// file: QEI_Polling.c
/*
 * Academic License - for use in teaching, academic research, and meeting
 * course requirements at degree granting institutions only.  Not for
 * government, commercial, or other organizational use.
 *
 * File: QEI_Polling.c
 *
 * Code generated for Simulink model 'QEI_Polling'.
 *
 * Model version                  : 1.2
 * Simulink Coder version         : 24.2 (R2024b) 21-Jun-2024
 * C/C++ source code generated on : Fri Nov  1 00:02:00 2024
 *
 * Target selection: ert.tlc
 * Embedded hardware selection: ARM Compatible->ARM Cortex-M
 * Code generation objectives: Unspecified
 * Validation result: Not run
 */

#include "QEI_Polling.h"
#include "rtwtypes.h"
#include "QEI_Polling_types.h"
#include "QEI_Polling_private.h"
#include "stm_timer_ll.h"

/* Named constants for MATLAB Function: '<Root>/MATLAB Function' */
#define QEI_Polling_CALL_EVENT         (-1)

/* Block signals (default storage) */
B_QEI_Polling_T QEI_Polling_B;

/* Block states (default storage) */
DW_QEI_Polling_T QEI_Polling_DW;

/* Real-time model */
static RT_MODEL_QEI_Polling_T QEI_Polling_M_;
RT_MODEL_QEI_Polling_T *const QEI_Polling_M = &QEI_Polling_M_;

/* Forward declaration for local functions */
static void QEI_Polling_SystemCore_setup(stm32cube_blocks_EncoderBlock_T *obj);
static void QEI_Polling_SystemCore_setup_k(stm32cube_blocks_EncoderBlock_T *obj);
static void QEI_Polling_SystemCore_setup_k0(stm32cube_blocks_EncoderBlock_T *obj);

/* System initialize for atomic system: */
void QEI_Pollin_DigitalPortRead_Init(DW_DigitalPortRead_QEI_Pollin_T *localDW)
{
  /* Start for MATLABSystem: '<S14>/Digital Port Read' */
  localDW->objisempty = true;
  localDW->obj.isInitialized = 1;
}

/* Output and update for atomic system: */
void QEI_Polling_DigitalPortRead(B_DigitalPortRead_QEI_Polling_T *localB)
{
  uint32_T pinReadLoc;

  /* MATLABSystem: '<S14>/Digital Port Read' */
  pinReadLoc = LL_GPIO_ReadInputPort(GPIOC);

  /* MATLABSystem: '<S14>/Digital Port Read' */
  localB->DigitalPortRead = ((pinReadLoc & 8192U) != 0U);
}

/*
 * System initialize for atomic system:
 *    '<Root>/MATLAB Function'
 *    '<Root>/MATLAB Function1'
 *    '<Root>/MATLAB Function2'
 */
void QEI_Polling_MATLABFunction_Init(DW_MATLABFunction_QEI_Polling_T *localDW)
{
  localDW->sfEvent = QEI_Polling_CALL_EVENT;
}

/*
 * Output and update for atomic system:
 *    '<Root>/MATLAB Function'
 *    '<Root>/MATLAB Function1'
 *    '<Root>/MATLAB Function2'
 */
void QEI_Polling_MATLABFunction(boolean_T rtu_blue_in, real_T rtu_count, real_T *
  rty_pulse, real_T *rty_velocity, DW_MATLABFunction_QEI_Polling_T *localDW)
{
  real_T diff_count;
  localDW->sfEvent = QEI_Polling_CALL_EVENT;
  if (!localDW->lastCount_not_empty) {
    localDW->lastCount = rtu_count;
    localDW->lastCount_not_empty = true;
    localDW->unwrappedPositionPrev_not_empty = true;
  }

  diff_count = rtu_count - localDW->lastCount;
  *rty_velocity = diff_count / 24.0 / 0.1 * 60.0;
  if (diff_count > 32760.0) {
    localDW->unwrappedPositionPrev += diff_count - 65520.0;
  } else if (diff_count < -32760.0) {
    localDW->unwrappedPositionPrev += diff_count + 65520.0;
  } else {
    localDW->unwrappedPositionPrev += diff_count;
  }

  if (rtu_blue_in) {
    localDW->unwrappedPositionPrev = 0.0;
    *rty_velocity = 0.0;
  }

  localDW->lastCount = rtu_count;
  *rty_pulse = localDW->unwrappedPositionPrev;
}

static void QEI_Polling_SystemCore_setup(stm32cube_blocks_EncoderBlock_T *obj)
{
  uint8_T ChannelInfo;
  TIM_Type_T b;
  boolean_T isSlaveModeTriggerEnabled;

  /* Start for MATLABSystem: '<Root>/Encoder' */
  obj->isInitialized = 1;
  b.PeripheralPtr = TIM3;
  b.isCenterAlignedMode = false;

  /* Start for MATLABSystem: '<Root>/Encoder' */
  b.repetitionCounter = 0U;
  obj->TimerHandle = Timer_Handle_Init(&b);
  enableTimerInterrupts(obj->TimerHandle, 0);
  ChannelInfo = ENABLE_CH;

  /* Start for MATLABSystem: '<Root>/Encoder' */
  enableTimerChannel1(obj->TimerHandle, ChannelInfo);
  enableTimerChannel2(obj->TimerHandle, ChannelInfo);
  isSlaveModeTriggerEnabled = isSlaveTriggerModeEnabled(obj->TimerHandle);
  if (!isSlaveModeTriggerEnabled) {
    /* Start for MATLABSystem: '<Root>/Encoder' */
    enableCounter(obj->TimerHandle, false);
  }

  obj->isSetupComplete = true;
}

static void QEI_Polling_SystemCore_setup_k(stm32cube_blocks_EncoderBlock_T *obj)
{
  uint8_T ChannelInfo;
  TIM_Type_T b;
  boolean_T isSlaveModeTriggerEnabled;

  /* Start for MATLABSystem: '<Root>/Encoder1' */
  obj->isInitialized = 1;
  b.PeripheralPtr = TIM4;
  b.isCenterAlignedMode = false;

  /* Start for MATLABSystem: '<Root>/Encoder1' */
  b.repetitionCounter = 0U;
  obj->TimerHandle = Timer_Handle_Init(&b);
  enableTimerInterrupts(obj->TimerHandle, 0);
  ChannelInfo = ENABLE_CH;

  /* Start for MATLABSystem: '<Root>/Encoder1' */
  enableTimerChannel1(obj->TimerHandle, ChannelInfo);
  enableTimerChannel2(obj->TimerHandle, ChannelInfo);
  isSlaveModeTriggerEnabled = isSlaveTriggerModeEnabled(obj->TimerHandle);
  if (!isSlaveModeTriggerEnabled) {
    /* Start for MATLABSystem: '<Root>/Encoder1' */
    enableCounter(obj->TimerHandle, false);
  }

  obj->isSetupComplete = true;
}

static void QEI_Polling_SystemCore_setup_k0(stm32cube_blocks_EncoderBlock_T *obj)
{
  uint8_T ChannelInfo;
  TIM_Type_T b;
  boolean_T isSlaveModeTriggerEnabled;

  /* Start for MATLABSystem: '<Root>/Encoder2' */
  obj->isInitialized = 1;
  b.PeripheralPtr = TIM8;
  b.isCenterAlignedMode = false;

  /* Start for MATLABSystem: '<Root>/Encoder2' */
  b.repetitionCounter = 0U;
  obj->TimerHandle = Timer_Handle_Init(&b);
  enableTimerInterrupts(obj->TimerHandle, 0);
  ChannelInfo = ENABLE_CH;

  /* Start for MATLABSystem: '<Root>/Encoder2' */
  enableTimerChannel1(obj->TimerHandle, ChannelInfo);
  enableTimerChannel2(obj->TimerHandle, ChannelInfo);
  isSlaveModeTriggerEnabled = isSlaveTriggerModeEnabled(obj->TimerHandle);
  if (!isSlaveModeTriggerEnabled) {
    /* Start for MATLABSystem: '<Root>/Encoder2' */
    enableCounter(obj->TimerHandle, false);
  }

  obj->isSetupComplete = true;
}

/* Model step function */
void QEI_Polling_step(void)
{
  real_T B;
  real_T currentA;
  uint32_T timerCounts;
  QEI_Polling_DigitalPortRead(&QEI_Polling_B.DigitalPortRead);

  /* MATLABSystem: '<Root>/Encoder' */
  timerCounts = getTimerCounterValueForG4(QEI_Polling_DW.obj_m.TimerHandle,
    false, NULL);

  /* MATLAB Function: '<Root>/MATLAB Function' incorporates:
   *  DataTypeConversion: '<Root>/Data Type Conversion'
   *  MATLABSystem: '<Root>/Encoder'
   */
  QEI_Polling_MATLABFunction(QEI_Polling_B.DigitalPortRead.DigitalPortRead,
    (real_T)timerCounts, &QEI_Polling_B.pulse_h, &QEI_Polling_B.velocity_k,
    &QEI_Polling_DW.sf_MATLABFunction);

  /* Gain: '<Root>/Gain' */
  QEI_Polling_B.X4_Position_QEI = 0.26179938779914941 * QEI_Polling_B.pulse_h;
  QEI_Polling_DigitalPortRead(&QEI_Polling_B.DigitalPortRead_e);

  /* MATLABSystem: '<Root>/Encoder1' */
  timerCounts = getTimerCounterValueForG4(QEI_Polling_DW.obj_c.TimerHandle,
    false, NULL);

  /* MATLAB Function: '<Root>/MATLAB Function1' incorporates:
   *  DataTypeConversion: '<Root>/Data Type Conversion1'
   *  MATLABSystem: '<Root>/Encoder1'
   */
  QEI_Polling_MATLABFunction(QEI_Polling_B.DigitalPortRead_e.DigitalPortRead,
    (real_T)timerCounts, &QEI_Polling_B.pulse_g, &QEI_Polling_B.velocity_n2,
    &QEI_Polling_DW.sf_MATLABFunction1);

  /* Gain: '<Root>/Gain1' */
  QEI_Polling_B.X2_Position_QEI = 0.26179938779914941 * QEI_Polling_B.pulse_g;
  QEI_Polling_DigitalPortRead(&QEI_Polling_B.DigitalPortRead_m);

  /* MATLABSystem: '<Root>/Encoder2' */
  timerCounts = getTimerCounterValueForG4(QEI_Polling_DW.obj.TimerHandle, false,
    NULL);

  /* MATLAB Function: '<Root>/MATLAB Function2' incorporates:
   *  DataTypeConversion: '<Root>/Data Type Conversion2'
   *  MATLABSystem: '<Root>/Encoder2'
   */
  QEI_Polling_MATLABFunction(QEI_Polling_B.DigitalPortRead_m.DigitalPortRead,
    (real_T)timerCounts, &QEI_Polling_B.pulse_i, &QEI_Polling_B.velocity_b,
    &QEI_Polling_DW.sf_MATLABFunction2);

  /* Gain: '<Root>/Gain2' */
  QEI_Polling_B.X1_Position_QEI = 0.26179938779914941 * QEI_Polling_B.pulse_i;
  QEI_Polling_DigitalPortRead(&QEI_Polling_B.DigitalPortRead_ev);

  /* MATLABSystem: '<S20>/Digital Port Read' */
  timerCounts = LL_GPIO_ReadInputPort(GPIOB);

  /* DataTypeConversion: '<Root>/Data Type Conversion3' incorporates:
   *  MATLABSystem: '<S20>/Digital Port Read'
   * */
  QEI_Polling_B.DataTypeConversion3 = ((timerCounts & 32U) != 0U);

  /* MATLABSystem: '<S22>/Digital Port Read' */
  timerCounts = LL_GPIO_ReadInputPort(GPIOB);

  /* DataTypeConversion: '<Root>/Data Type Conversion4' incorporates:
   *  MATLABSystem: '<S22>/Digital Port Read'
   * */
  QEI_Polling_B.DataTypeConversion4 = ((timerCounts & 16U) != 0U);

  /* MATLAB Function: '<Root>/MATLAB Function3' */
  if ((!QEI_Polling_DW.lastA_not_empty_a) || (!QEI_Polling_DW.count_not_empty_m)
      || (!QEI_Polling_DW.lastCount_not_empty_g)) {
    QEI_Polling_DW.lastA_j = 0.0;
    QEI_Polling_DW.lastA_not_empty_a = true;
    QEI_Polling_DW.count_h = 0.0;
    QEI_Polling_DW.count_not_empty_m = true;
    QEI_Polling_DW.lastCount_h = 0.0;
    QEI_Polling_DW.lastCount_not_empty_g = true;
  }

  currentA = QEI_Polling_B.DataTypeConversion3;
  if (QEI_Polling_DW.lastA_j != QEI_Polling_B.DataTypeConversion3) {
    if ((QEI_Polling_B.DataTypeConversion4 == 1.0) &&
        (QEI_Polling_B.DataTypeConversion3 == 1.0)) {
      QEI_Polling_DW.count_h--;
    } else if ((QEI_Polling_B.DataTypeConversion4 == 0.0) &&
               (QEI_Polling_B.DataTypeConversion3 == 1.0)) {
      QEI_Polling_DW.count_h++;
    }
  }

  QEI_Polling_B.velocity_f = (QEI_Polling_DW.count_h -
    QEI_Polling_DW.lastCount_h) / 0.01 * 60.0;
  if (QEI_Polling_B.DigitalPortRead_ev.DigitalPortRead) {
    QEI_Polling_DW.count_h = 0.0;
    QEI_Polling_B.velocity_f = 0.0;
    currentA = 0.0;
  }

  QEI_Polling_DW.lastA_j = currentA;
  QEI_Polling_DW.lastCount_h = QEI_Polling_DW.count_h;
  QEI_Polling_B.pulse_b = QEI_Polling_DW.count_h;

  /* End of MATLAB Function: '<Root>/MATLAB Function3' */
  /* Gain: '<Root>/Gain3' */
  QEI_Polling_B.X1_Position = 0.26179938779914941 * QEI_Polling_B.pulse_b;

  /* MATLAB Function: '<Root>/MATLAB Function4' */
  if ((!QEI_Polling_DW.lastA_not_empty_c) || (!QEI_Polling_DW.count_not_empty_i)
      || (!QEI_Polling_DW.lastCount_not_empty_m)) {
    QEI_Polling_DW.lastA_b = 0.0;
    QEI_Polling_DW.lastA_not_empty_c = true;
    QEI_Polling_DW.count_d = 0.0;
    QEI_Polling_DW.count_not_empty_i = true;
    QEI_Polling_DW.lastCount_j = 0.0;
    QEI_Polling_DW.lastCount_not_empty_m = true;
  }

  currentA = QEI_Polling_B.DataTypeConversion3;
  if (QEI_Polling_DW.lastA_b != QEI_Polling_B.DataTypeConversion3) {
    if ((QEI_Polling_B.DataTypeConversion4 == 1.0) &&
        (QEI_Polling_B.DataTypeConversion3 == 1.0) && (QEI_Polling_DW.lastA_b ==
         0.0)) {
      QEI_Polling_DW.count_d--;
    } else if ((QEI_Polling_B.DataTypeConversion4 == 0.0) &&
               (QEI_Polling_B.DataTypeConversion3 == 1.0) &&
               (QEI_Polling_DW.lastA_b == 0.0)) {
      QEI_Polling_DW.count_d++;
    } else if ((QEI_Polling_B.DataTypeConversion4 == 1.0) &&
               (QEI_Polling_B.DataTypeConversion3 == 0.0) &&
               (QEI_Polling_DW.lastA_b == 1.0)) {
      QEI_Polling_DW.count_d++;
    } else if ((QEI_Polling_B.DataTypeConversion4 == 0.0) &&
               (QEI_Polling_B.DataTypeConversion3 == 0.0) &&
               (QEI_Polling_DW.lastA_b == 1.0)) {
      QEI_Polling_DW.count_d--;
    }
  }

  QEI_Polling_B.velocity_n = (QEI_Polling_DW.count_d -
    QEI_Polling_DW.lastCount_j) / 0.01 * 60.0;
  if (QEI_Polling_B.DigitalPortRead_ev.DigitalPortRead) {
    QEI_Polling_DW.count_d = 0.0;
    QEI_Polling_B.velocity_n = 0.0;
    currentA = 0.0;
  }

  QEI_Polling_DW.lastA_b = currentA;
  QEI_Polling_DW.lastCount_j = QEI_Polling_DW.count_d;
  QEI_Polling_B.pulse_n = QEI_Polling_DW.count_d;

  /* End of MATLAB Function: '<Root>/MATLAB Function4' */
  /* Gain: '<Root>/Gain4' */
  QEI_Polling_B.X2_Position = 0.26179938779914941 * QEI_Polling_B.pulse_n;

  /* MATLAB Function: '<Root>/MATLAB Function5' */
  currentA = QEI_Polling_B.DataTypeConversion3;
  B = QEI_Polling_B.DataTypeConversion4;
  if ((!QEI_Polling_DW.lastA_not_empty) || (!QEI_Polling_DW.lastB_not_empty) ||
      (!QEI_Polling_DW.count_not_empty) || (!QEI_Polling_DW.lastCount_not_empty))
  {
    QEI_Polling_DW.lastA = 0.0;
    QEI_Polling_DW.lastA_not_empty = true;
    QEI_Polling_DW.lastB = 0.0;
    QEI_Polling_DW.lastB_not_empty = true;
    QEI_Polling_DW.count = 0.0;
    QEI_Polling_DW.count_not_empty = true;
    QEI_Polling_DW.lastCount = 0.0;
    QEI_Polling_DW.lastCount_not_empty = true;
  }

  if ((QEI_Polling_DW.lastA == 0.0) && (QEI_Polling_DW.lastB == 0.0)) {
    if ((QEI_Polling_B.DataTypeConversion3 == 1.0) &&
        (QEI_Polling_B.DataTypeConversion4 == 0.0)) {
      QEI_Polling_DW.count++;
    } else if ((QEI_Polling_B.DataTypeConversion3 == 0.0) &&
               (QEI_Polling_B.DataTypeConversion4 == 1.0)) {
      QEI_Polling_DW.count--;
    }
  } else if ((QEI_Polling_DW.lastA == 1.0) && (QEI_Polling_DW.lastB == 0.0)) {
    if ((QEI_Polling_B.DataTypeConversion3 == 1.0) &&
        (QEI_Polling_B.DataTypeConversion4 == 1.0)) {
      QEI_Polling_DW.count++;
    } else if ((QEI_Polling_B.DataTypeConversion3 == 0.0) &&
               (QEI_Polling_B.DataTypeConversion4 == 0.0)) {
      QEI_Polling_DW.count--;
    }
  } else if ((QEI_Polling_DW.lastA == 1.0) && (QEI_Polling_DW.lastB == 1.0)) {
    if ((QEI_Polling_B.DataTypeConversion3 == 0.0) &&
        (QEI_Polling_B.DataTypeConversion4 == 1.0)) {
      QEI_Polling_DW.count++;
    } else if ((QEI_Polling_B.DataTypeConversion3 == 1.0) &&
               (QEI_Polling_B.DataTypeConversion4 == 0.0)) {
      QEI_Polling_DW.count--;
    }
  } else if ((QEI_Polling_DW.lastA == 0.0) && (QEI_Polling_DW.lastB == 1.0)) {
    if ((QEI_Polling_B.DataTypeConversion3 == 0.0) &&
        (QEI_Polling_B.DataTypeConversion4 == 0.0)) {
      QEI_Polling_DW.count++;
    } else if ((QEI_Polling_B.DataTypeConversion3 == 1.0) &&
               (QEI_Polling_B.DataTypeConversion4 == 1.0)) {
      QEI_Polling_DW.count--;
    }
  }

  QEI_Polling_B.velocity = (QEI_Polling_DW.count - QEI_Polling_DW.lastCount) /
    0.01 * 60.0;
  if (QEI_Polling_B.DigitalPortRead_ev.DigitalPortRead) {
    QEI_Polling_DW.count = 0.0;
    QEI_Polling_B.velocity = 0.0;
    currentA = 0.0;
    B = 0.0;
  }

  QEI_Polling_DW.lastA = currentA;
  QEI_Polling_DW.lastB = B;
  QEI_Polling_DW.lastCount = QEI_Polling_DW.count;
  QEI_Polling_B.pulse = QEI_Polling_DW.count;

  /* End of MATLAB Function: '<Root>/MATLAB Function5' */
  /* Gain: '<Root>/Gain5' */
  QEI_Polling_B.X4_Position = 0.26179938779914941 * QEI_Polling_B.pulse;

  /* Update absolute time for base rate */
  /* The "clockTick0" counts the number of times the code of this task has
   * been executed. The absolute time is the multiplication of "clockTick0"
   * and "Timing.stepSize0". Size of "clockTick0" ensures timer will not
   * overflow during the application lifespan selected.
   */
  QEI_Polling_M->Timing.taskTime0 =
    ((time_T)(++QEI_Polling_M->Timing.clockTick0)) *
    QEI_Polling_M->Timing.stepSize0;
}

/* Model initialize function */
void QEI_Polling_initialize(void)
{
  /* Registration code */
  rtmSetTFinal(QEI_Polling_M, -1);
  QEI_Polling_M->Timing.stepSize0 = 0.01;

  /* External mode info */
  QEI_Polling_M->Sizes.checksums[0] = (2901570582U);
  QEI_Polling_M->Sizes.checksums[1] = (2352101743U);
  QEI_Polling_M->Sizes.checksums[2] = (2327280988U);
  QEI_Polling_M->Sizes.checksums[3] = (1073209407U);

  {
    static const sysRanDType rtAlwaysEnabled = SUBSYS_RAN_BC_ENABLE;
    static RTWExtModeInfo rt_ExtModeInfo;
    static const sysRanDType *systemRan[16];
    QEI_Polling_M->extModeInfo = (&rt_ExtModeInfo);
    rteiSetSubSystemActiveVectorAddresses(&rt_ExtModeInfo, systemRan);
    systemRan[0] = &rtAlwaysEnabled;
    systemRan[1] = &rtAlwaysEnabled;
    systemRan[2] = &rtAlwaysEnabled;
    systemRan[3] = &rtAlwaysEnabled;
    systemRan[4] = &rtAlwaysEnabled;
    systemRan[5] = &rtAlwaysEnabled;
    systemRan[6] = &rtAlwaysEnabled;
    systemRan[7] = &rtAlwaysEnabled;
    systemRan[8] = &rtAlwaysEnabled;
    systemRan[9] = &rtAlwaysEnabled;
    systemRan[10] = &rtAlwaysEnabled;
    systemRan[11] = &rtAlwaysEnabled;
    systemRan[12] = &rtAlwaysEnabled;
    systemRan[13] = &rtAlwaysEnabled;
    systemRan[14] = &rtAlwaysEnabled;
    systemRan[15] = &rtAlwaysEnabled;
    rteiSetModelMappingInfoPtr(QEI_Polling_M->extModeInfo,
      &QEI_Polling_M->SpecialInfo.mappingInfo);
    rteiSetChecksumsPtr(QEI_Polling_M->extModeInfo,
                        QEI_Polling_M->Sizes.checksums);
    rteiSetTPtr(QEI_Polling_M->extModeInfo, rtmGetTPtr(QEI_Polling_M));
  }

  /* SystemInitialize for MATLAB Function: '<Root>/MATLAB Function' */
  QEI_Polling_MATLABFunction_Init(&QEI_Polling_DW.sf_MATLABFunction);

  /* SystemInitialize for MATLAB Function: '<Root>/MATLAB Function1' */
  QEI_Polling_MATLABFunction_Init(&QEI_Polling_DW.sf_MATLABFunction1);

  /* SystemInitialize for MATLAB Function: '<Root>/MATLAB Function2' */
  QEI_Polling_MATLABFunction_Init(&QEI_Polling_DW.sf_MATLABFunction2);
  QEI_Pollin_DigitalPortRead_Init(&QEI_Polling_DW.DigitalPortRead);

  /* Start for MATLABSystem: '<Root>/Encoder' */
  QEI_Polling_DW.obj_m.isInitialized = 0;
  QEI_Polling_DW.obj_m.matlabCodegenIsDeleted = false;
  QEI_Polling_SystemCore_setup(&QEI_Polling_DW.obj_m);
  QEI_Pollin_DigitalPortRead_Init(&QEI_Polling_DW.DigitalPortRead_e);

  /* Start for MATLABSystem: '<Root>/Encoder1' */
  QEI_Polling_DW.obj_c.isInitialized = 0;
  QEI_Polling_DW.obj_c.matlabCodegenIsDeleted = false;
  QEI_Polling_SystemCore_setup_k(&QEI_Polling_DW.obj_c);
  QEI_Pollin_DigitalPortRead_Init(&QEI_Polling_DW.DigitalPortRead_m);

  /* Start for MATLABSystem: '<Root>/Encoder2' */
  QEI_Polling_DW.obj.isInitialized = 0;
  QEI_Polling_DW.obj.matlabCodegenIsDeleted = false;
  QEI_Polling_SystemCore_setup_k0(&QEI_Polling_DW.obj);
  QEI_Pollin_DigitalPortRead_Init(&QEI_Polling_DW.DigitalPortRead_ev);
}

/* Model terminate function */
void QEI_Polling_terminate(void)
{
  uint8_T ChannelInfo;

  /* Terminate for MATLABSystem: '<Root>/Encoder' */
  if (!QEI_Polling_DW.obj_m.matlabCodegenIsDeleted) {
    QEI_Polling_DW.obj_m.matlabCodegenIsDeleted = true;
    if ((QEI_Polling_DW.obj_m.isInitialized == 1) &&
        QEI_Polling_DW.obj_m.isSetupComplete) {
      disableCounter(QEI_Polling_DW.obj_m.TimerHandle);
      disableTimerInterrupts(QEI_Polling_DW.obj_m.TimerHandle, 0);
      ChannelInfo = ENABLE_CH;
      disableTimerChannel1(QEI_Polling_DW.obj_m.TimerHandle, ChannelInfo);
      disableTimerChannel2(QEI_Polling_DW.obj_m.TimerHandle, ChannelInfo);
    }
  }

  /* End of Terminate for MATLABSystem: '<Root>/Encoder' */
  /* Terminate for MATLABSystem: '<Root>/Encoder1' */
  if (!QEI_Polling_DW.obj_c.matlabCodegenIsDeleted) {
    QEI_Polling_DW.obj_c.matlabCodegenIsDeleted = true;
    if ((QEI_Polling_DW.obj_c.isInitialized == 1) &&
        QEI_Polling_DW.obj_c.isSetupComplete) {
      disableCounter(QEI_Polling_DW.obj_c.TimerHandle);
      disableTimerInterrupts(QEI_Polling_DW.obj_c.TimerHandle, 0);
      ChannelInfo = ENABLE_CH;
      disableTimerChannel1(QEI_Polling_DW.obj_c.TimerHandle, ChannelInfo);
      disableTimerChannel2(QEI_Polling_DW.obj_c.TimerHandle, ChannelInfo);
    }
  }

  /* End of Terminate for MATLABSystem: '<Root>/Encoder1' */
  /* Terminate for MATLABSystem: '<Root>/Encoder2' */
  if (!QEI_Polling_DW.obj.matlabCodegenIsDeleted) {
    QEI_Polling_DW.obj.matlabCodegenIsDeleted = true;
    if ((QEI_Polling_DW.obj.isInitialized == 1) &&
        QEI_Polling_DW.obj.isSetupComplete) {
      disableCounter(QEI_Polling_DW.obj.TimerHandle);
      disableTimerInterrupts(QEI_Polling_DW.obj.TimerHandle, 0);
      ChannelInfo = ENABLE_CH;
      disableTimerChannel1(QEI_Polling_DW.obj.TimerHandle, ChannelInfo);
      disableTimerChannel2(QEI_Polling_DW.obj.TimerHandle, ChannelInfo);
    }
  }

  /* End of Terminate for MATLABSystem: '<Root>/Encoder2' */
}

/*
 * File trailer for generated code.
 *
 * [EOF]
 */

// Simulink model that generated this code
simulink model "QEI_Polling"  (R2024b)
settings: Solver=FixedStepAuto  StartTime=0.0  StopTime=inf  FixedStep=0.001  RelTol=1e-3  EnableMultiTasking=on
libraries: stm32f4xxblockslib x5, stm32g4xxblockslib x3

== system QEI_Polling ==
  note: QEI
  Data Type Conversion{,1..4} (5 alike) : DataTypeConversion  OutDataTypeStr=double  SaturateOnIntegerOverflow=off  RndMeth=Floor
  Digital Port Read : stm32f4xxblockslib/Digital Port Read  PortName=GPIOC  PinNumber=[13]  ReadOperation=on  IOAsArray=on  SampleTime=-1  EnableSimPort=off  hoistedMaskSrc=ECSoC/ECSimCodegen/Digital Port Read
  Digital Port Read1 : stm32f4xxblockslib/Digital Port Read  PortName=GPIOC  PinNumber=[13]  ReadOperation=on  IOAsArray=on  SampleTime=-1  EnableSimPort=off  hoistedMaskSrc=ECSoC/ECSimCodegen/Digital Port Read
  Digital Port Read2 : stm32f4xxblockslib/Digital Port Read  PortName=GPIOC  PinNumber=[13]  ReadOperation=on  IOAsArray=on  SampleTime=-1  EnableSimPort=off  hoistedMaskSrc=ECSoC/ECSimCodegen/Digital Port Read
  Digital Port Read3 : stm32f4xxblockslib/Digital Port Read  PortName=GPIOB  PinNumber=[5]  ReadOperation=on  IOAsArray=on  SampleTime=-1  EnableSimPort=off  hoistedMaskSrc=ECSoC/ECSimCodegen/Digital Port Read
  Digital Port Read4 : stm32f4xxblockslib/Digital Port Read  PortName=GPIOB  PinNumber=[4]  ReadOperation=on  IOAsArray=on  SampleTime=-1  EnableSimPort=off  hoistedMaskSrc=ECSoC/ECSimCodegen/Digital Port Read
  Display{,1..17} (18 alike) : Display
  Encoder : stm32g4xxblockslib/Encoder  TimerModule=TIM3  EnableResetInput=off  OutputCountAfterFirstIndex=off  OutputValidIndex=off  OutputDirection=off  OutputStatus=off  SampleTime=-1
  Encoder1 : stm32g4xxblockslib/Encoder  TimerModule=TIM4  EnableResetInput=off  OutputCountAfterFirstIndex=off  OutputValidIndex=off  OutputDirection=off  OutputStatus=off  SampleTime=-1
  Encoder2 : stm32g4xxblockslib/Encoder  TimerModule=TIM8  EnableResetInput=off  OutputCountAfterFirstIndex=off  OutputValidIndex=off  OutputDirection=off  OutputStatus=off  SampleTime=-1
  Gain{,1..5} (6 alike) : Gain  Gain=(2 * pi)/24
  MATLAB Function : MATLAB Function  TreatAsAtomicUnit=on
  MATLAB Function1 : MATLAB Function  TreatAsAtomicUnit=on
  MATLAB Function2 : MATLAB Function  TreatAsAtomicUnit=on
  MATLAB Function3 : MATLAB Function  TreatAsAtomicUnit=on
  MATLAB Function4 : MATLAB Function  TreatAsAtomicUnit=on
  MATLAB Function5 : MATLAB Function  TreatAsAtomicUnit=on
  wires:
  Data Type Conversion/1 -> MATLAB Function/2(count)
  Encoder1/1 -> Data Type Conversion1/1
  Gain3/1 -> Display10/1  "X1_Position"
  MATLAB Function2/2(velocity) -> Display7/1  "X1_Velocity_QEI"
  MATLAB Function3/2(velocity) -> Display9/1  "X1_Velocity"
  Data Type Conversion3/1 -> MATLAB Function4/1(A), MATLAB Function5/1(A), MATLAB Function3/1(A)
  Data Type Conversion2/1 -> MATLAB Function2/2(count)
  MATLAB Function3/1(pulse) -> Display11/1, Gain3/1  "X1_Pulse"
  Digital Port Read1/1 -> MATLAB Function1/1(blue_in)
  Encoder2/1 -> Data Type Conversion2/1
  Digital Port Read/1 -> MATLAB Function/1(blue_in)
  Digital Port Read4/1 -> Data Type Conversion4/1
  MATLAB Function5/1(pulse) -> Display16/1, Gain5/1  "X4_Pulse"
  MATLAB Function/1(pulse) -> Display2/1, Gain/1  "X4_Pulse_QEI"
  Gain5/1 -> Display15/1  "X4_Position"
  Data Type Conversion1/1 -> MATLAB Function1/2(count)
  MATLAB Function1/2(velocity) -> Display4/1  "X2_Velocity_QEI"
  Data Type Conversion4/1 -> MATLAB Function4/2(B), MATLAB Function5/2(B), MATLAB Function3/2(B)
  Gain1/1 -> Display3/1  "X2_Position_QEI"
  Digital Port Read3/1 -> Data Type Conversion3/1
  MATLAB Function4/1(pulse) -> Display13/1, Gain4/1  "X2_Pulse"
  Encoder/1 -> Data Type Conversion/1
  Digital Port Read2/1 -> MATLAB Function2/1(blue_in)
  MATLAB Function5/2(velocity) -> Display17/1  "X4_Velocity"
  MATLAB Function1/1(pulse) -> Display5/1, Gain1/1  "X2_Pulse_QEI"
  Gain/1 -> Display/1  "X4_Position_QEI"
  MATLAB Function/2(velocity) -> Display1/1  "X4_Velocity_QEI"
  Gain4/1 -> Display12/1  "X2_Position"
  Gain2/1 -> Display6/1  "X1_Position_QEI"
  MATLAB Function4/2(velocity) -> Display14/1  "X2_Velocity"
  MATLAB Function2/1(pulse) -> Display8/1, Gain2/1  "X1_Pulse_QEI"

== matlab function QEI_Polling/MATLAB Function1 ==
function [pulse, velocity] = X4(blue_in, count)
    %#codegen
    
    % ประกาศตัวแปร persistent เพื่อเก็บค่าตัวนับก่อนหน้าและตำแหน่งที่คลายห่อก่อนหน้า
    persistent previousCount unwrappedPositionPrev;
    
    % กำหนดค่าเริ่มต้นให้ตัวแปร persistent เมื่อเรียกใช้งานครั้งแรก
    if isempty(previousCount)
        previousCount = count;
        unwrappedPositionPrev = 0;  % กำหนดตำแหน่งคลายห่อเริ่มต้นเป็นศูนย์
    end

    % กำหนดขอบเขตของ encoder
    encoderMax = 65520;   % ค่าสูงสุดสำหรับ encoder แบบ 16-bit (0-65535)
    threshold = encoderMax / 2;  % ค่า threshold สำหรับตรวจจับ overflow หรือ underflow

    % คำนวณค่าความแตกต่างระหว่างค่าปัจจุบันกับค่าก่อนหน้า
    diff_count = count - previousCount;

    % คำนวณความเร็วเชิงมุม (Angular Velocity)
    Ts = 0.01; % กำหนด Sampling Time (เช่น 10ms)
    PPR = 24; % จำนวนพัลส์ต่อรอบ
    velocity = ((diff_count / PPR) / Ts) * 60; % Velocity เป็น RPM

    % ตรวจจับการ overflow และ underflow
    if diff_count > threshold
        % พบการ overflow (เช่น count เปลี่ยนจาก 65535 กลับไปที่ 0)
        pulse = unwrappedPositionPrev + (diff_count - encoderMax);
    elseif diff_count < -threshold
        % พบการ underflow (เช่น count เปลี่ยนจาก 0 เป็น 65535)
        pulse = unwrappedPositionPrev + (diff_count + encoderMax);
    else
        % กรณีปกติที่ไม่มี overflow/underflow
        pulse = unwrappedPositionPrev + diff_count;
    end

    if blue_in == 1
        pulse = 0;
        velocity = 0;
    end
    % อัปเดตตัวแปร persistent เพื่อใช้ในรอบถัดไป
    previousCount = count;
    unwrappedPositionPrev = pulse; 
end

== matlab function QEI_Polling/MATLAB Function ==
function [pulse, velocity] = X4(blue_in, count)
    %#codegen
    
    % ประกาศตัวแปร persistent เพื่อเก็บค่าตัวนับก่อนหน้าและตำแหน่งที่คลายห่อก่อนหน้า
    persistent previousCount unwrappedPositionPrev;
    
    % กำหนดค่าเริ่มต้นให้ตัวแปร persistent เมื่อเรียกใช้งานครั้งแรก
    if isempty(previousCount)
        previousCount = count;
        unwrappedPositionPrev = 0;  % กำหนดตำแหน่งคลายห่อเริ่มต้นเป็นศูนย์
    end

    % กำหนดขอบเขตของ encoder
    encoderMax = 65520;   % ค่าสูงสุดสำหรับ encoder แบบ 16-bit (0-65535)
    threshold = encoderMax / 2;  % ค่า threshold สำหรับตรวจจับ overflow หรือ underflow

    % คำนวณค่าความแตกต่างระหว่างค่าปัจจุบันกับค่าก่อนหน้า
    diff_count = count - previousCount;

    % คำนวณความเร็วเชิงมุม (Angular Velocity)
    Ts = 0.01; % กำหนด Sampling Time (เช่น 10ms)
    PPR = 24; % จำนวนพัลส์ต่อรอบ
    velocity = ((diff_count / PPR) / Ts) * 60; % Velocity เป็น RPM

    % ตรวจจับการ overflow และ underflow
    if diff_count > threshold
        % พบการ overflow (เช่น count เปลี่ยนจาก 65535 กลับไปที่ 0)
        pulse = unwrappedPositionPrev + (diff_count - encoderMax);
    elseif diff_count < -threshold
        % พบการ underflow (เช่น count เปลี่ยนจาก 0 เป็น 65535)
        pulse = unwrappedPositionPrev + (diff_count + encoderMax);
    else
        % กรณีปกติที่ไม่มี overflow/underflow
        pulse = unwrappedPositionPrev + diff_count;
    end

    if blue_in == 1
        pulse = 0;
        velocity = 0;
    end
    % อัปเดตตัวแปร persistent เพื่อใช้ในรอบถัดไป
    previousCount = count;
    unwrappedPositionPrev = pulse; 
end

== matlab function QEI_Polling/MATLAB Function2 ==
function [pulse, velocity] = X1(blue_in, count)
    %#codegen
    
    % ประกาศตัวแปร persistent เพื่อเก็บค่าตัวนับก่อนหน้าและตำแหน่งที่คลายห่อก่อนหน้า
    persistent previousCount unwrappedPositionPrev;
    
    % กำหนดค่าเริ่มต้นให้ตัวแปร persistent เมื่อเรียกใช้งานครั้งแรก
    if isempty(previousCount)
        previousCount = count;
        unwrappedPositionPrev = 0;  % กำหนดตำแหน่งคลายห่อเริ่มต้นเป็นศูนย์
    end

    % กำหนดขอบเขตของ encoder
    encoderMax = 65520;   % ค่าสูงสุดสำหรับ encoder แบบ 16-bit (0-65535)
    threshold = encoderMax / 2;  % ค่า threshold สำหรับตรวจจับ overflow หรือ underflow

    % คำนวณค่าความแตกต่างระหว่างค่าปัจจุบันกับค่าก่อนหน้า
    diff_count = count - previousCount;

    % คำนวณความเร็วเชิงมุม (Angular Velocity)
    Ts = 0.01; % กำหนด Sampling Time (เช่น 10ms)
    PPR = 24; % จำนวนพัลส์ต่อรอบ
    velocity = ((diff_count / PPR) / Ts) * 60; % Velocity เป็น RPM

    % ตรวจจับการ overflow และ underflow
    if diff_count > threshold
        % พบการ overflow (เช่น count เปลี่ยนจาก 65535 กลับไปที่ 0)
        pulse = unwrappedPositionPrev + (diff_count - encoderMax);
    elseif diff_count < -threshold
        % พบการ underflow (เช่น count เปลี่ยนจาก 0 เป็น 65535)
        pulse = unwrappedPositionPrev + (diff_count + encoderMax);
    else
        % กรณีปกติที่ไม่มี overflow/underflow
        pulse = unwrappedPositionPrev + diff_count;
    end

    if blue_in == 1
        pulse = 0;
        velocity = 0;
    end
    % อัปเดตตัวแปร persistent เพื่อใช้ในรอบถัดไป
    previousCount = count;
    unwrappedPositionPrev = pulse; 
end

== matlab function QEI_Polling/MATLAB Function3 ==
function [pulse, velocity] = EncoderX1(A, B)
   
    persistent lastA count lastCount;
    if isempty(lastA) || isempty(count) || isempty(lastCount)
        lastA = 0;
        count = 0;
        lastCount = 0;
    end
    
    currentA = A;  
    currentB = B;  
    
    if lastA ~= currentA
        if currentB == 1 && currentA == 1
            count = count - 1; 
        elseif currentB == 0 && currentA == 1
            count = count + 1;  
        end
    end
    
    velocity = ((count - lastCount) / 0.001) * 60;
    
    lastA = currentA;
    lastCount = count;
    
    pulse = count;
end

== matlab function QEI_Polling/MATLAB Function4 ==
function [pulse, velocity] = EncoderX2(A, B)
   
    persistent lastA count lastCount;
    if isempty(lastA) || isempty(count) || isempty(lastCount)
        lastA = 0;
        count = 0;
        lastCount = 0;
    end
    
    currentA = A;  
    currentB = B;  
    
    if lastA ~= currentA
        if currentB == 1 && currentA == 1 && lastA == 0
            count = count - 1;  % Forward count
        elseif currentB == 0 && currentA == 1 && lastA == 0
            count = count + 1;  % Backward count
        elseif currentB == 1 && currentA == 0 && lastA == 1
            count = count + 1;
        elseif currentB == 0 && currentA == 0 && lastA == 1
            count = count - 1;
        end
    end
    
    velocity = ((count - lastCount) / 0.001) * 60;
    
    lastA = currentA;
    lastCount = count;
    
    pulse = count;
end

== matlab function QEI_Polling/MATLAB Function5 ==
function [pulse, velocity] = EncoderX4(A, B)

    persistent lastA lastB count lastCount;

    if isempty(lastA) || isempty(lastB) || isempty(count) || isempty(lastCount)
        lastA = 0;
        lastB = 0;
        count = 0;
        lastCount = 0;
    end
    
    
    if lastA == 0 && A == 1
        if B  == 0
            count = count + 1;
        else
            count = count - 1;
        end
    elseif lastA == 1 && A == 0
        if B == 0
            count = count - 1;
        else
            count = count + 1;
        end
    elseif lastB == 0 && B == 1
        if A == 0
            count = count + 1;
        else
            count = count - 1;
        end
    elseif lastB == 1 && B == 0
        if A == 0
            count = count - 1;
        else
            count = count + 1;
        end
    end
        
    
    velocity = ((count - lastCount) / 0.001) * 60;
    
    lastA = A;
    lastB = B;
    lastCount = count;
    
    pulse = count;
end
